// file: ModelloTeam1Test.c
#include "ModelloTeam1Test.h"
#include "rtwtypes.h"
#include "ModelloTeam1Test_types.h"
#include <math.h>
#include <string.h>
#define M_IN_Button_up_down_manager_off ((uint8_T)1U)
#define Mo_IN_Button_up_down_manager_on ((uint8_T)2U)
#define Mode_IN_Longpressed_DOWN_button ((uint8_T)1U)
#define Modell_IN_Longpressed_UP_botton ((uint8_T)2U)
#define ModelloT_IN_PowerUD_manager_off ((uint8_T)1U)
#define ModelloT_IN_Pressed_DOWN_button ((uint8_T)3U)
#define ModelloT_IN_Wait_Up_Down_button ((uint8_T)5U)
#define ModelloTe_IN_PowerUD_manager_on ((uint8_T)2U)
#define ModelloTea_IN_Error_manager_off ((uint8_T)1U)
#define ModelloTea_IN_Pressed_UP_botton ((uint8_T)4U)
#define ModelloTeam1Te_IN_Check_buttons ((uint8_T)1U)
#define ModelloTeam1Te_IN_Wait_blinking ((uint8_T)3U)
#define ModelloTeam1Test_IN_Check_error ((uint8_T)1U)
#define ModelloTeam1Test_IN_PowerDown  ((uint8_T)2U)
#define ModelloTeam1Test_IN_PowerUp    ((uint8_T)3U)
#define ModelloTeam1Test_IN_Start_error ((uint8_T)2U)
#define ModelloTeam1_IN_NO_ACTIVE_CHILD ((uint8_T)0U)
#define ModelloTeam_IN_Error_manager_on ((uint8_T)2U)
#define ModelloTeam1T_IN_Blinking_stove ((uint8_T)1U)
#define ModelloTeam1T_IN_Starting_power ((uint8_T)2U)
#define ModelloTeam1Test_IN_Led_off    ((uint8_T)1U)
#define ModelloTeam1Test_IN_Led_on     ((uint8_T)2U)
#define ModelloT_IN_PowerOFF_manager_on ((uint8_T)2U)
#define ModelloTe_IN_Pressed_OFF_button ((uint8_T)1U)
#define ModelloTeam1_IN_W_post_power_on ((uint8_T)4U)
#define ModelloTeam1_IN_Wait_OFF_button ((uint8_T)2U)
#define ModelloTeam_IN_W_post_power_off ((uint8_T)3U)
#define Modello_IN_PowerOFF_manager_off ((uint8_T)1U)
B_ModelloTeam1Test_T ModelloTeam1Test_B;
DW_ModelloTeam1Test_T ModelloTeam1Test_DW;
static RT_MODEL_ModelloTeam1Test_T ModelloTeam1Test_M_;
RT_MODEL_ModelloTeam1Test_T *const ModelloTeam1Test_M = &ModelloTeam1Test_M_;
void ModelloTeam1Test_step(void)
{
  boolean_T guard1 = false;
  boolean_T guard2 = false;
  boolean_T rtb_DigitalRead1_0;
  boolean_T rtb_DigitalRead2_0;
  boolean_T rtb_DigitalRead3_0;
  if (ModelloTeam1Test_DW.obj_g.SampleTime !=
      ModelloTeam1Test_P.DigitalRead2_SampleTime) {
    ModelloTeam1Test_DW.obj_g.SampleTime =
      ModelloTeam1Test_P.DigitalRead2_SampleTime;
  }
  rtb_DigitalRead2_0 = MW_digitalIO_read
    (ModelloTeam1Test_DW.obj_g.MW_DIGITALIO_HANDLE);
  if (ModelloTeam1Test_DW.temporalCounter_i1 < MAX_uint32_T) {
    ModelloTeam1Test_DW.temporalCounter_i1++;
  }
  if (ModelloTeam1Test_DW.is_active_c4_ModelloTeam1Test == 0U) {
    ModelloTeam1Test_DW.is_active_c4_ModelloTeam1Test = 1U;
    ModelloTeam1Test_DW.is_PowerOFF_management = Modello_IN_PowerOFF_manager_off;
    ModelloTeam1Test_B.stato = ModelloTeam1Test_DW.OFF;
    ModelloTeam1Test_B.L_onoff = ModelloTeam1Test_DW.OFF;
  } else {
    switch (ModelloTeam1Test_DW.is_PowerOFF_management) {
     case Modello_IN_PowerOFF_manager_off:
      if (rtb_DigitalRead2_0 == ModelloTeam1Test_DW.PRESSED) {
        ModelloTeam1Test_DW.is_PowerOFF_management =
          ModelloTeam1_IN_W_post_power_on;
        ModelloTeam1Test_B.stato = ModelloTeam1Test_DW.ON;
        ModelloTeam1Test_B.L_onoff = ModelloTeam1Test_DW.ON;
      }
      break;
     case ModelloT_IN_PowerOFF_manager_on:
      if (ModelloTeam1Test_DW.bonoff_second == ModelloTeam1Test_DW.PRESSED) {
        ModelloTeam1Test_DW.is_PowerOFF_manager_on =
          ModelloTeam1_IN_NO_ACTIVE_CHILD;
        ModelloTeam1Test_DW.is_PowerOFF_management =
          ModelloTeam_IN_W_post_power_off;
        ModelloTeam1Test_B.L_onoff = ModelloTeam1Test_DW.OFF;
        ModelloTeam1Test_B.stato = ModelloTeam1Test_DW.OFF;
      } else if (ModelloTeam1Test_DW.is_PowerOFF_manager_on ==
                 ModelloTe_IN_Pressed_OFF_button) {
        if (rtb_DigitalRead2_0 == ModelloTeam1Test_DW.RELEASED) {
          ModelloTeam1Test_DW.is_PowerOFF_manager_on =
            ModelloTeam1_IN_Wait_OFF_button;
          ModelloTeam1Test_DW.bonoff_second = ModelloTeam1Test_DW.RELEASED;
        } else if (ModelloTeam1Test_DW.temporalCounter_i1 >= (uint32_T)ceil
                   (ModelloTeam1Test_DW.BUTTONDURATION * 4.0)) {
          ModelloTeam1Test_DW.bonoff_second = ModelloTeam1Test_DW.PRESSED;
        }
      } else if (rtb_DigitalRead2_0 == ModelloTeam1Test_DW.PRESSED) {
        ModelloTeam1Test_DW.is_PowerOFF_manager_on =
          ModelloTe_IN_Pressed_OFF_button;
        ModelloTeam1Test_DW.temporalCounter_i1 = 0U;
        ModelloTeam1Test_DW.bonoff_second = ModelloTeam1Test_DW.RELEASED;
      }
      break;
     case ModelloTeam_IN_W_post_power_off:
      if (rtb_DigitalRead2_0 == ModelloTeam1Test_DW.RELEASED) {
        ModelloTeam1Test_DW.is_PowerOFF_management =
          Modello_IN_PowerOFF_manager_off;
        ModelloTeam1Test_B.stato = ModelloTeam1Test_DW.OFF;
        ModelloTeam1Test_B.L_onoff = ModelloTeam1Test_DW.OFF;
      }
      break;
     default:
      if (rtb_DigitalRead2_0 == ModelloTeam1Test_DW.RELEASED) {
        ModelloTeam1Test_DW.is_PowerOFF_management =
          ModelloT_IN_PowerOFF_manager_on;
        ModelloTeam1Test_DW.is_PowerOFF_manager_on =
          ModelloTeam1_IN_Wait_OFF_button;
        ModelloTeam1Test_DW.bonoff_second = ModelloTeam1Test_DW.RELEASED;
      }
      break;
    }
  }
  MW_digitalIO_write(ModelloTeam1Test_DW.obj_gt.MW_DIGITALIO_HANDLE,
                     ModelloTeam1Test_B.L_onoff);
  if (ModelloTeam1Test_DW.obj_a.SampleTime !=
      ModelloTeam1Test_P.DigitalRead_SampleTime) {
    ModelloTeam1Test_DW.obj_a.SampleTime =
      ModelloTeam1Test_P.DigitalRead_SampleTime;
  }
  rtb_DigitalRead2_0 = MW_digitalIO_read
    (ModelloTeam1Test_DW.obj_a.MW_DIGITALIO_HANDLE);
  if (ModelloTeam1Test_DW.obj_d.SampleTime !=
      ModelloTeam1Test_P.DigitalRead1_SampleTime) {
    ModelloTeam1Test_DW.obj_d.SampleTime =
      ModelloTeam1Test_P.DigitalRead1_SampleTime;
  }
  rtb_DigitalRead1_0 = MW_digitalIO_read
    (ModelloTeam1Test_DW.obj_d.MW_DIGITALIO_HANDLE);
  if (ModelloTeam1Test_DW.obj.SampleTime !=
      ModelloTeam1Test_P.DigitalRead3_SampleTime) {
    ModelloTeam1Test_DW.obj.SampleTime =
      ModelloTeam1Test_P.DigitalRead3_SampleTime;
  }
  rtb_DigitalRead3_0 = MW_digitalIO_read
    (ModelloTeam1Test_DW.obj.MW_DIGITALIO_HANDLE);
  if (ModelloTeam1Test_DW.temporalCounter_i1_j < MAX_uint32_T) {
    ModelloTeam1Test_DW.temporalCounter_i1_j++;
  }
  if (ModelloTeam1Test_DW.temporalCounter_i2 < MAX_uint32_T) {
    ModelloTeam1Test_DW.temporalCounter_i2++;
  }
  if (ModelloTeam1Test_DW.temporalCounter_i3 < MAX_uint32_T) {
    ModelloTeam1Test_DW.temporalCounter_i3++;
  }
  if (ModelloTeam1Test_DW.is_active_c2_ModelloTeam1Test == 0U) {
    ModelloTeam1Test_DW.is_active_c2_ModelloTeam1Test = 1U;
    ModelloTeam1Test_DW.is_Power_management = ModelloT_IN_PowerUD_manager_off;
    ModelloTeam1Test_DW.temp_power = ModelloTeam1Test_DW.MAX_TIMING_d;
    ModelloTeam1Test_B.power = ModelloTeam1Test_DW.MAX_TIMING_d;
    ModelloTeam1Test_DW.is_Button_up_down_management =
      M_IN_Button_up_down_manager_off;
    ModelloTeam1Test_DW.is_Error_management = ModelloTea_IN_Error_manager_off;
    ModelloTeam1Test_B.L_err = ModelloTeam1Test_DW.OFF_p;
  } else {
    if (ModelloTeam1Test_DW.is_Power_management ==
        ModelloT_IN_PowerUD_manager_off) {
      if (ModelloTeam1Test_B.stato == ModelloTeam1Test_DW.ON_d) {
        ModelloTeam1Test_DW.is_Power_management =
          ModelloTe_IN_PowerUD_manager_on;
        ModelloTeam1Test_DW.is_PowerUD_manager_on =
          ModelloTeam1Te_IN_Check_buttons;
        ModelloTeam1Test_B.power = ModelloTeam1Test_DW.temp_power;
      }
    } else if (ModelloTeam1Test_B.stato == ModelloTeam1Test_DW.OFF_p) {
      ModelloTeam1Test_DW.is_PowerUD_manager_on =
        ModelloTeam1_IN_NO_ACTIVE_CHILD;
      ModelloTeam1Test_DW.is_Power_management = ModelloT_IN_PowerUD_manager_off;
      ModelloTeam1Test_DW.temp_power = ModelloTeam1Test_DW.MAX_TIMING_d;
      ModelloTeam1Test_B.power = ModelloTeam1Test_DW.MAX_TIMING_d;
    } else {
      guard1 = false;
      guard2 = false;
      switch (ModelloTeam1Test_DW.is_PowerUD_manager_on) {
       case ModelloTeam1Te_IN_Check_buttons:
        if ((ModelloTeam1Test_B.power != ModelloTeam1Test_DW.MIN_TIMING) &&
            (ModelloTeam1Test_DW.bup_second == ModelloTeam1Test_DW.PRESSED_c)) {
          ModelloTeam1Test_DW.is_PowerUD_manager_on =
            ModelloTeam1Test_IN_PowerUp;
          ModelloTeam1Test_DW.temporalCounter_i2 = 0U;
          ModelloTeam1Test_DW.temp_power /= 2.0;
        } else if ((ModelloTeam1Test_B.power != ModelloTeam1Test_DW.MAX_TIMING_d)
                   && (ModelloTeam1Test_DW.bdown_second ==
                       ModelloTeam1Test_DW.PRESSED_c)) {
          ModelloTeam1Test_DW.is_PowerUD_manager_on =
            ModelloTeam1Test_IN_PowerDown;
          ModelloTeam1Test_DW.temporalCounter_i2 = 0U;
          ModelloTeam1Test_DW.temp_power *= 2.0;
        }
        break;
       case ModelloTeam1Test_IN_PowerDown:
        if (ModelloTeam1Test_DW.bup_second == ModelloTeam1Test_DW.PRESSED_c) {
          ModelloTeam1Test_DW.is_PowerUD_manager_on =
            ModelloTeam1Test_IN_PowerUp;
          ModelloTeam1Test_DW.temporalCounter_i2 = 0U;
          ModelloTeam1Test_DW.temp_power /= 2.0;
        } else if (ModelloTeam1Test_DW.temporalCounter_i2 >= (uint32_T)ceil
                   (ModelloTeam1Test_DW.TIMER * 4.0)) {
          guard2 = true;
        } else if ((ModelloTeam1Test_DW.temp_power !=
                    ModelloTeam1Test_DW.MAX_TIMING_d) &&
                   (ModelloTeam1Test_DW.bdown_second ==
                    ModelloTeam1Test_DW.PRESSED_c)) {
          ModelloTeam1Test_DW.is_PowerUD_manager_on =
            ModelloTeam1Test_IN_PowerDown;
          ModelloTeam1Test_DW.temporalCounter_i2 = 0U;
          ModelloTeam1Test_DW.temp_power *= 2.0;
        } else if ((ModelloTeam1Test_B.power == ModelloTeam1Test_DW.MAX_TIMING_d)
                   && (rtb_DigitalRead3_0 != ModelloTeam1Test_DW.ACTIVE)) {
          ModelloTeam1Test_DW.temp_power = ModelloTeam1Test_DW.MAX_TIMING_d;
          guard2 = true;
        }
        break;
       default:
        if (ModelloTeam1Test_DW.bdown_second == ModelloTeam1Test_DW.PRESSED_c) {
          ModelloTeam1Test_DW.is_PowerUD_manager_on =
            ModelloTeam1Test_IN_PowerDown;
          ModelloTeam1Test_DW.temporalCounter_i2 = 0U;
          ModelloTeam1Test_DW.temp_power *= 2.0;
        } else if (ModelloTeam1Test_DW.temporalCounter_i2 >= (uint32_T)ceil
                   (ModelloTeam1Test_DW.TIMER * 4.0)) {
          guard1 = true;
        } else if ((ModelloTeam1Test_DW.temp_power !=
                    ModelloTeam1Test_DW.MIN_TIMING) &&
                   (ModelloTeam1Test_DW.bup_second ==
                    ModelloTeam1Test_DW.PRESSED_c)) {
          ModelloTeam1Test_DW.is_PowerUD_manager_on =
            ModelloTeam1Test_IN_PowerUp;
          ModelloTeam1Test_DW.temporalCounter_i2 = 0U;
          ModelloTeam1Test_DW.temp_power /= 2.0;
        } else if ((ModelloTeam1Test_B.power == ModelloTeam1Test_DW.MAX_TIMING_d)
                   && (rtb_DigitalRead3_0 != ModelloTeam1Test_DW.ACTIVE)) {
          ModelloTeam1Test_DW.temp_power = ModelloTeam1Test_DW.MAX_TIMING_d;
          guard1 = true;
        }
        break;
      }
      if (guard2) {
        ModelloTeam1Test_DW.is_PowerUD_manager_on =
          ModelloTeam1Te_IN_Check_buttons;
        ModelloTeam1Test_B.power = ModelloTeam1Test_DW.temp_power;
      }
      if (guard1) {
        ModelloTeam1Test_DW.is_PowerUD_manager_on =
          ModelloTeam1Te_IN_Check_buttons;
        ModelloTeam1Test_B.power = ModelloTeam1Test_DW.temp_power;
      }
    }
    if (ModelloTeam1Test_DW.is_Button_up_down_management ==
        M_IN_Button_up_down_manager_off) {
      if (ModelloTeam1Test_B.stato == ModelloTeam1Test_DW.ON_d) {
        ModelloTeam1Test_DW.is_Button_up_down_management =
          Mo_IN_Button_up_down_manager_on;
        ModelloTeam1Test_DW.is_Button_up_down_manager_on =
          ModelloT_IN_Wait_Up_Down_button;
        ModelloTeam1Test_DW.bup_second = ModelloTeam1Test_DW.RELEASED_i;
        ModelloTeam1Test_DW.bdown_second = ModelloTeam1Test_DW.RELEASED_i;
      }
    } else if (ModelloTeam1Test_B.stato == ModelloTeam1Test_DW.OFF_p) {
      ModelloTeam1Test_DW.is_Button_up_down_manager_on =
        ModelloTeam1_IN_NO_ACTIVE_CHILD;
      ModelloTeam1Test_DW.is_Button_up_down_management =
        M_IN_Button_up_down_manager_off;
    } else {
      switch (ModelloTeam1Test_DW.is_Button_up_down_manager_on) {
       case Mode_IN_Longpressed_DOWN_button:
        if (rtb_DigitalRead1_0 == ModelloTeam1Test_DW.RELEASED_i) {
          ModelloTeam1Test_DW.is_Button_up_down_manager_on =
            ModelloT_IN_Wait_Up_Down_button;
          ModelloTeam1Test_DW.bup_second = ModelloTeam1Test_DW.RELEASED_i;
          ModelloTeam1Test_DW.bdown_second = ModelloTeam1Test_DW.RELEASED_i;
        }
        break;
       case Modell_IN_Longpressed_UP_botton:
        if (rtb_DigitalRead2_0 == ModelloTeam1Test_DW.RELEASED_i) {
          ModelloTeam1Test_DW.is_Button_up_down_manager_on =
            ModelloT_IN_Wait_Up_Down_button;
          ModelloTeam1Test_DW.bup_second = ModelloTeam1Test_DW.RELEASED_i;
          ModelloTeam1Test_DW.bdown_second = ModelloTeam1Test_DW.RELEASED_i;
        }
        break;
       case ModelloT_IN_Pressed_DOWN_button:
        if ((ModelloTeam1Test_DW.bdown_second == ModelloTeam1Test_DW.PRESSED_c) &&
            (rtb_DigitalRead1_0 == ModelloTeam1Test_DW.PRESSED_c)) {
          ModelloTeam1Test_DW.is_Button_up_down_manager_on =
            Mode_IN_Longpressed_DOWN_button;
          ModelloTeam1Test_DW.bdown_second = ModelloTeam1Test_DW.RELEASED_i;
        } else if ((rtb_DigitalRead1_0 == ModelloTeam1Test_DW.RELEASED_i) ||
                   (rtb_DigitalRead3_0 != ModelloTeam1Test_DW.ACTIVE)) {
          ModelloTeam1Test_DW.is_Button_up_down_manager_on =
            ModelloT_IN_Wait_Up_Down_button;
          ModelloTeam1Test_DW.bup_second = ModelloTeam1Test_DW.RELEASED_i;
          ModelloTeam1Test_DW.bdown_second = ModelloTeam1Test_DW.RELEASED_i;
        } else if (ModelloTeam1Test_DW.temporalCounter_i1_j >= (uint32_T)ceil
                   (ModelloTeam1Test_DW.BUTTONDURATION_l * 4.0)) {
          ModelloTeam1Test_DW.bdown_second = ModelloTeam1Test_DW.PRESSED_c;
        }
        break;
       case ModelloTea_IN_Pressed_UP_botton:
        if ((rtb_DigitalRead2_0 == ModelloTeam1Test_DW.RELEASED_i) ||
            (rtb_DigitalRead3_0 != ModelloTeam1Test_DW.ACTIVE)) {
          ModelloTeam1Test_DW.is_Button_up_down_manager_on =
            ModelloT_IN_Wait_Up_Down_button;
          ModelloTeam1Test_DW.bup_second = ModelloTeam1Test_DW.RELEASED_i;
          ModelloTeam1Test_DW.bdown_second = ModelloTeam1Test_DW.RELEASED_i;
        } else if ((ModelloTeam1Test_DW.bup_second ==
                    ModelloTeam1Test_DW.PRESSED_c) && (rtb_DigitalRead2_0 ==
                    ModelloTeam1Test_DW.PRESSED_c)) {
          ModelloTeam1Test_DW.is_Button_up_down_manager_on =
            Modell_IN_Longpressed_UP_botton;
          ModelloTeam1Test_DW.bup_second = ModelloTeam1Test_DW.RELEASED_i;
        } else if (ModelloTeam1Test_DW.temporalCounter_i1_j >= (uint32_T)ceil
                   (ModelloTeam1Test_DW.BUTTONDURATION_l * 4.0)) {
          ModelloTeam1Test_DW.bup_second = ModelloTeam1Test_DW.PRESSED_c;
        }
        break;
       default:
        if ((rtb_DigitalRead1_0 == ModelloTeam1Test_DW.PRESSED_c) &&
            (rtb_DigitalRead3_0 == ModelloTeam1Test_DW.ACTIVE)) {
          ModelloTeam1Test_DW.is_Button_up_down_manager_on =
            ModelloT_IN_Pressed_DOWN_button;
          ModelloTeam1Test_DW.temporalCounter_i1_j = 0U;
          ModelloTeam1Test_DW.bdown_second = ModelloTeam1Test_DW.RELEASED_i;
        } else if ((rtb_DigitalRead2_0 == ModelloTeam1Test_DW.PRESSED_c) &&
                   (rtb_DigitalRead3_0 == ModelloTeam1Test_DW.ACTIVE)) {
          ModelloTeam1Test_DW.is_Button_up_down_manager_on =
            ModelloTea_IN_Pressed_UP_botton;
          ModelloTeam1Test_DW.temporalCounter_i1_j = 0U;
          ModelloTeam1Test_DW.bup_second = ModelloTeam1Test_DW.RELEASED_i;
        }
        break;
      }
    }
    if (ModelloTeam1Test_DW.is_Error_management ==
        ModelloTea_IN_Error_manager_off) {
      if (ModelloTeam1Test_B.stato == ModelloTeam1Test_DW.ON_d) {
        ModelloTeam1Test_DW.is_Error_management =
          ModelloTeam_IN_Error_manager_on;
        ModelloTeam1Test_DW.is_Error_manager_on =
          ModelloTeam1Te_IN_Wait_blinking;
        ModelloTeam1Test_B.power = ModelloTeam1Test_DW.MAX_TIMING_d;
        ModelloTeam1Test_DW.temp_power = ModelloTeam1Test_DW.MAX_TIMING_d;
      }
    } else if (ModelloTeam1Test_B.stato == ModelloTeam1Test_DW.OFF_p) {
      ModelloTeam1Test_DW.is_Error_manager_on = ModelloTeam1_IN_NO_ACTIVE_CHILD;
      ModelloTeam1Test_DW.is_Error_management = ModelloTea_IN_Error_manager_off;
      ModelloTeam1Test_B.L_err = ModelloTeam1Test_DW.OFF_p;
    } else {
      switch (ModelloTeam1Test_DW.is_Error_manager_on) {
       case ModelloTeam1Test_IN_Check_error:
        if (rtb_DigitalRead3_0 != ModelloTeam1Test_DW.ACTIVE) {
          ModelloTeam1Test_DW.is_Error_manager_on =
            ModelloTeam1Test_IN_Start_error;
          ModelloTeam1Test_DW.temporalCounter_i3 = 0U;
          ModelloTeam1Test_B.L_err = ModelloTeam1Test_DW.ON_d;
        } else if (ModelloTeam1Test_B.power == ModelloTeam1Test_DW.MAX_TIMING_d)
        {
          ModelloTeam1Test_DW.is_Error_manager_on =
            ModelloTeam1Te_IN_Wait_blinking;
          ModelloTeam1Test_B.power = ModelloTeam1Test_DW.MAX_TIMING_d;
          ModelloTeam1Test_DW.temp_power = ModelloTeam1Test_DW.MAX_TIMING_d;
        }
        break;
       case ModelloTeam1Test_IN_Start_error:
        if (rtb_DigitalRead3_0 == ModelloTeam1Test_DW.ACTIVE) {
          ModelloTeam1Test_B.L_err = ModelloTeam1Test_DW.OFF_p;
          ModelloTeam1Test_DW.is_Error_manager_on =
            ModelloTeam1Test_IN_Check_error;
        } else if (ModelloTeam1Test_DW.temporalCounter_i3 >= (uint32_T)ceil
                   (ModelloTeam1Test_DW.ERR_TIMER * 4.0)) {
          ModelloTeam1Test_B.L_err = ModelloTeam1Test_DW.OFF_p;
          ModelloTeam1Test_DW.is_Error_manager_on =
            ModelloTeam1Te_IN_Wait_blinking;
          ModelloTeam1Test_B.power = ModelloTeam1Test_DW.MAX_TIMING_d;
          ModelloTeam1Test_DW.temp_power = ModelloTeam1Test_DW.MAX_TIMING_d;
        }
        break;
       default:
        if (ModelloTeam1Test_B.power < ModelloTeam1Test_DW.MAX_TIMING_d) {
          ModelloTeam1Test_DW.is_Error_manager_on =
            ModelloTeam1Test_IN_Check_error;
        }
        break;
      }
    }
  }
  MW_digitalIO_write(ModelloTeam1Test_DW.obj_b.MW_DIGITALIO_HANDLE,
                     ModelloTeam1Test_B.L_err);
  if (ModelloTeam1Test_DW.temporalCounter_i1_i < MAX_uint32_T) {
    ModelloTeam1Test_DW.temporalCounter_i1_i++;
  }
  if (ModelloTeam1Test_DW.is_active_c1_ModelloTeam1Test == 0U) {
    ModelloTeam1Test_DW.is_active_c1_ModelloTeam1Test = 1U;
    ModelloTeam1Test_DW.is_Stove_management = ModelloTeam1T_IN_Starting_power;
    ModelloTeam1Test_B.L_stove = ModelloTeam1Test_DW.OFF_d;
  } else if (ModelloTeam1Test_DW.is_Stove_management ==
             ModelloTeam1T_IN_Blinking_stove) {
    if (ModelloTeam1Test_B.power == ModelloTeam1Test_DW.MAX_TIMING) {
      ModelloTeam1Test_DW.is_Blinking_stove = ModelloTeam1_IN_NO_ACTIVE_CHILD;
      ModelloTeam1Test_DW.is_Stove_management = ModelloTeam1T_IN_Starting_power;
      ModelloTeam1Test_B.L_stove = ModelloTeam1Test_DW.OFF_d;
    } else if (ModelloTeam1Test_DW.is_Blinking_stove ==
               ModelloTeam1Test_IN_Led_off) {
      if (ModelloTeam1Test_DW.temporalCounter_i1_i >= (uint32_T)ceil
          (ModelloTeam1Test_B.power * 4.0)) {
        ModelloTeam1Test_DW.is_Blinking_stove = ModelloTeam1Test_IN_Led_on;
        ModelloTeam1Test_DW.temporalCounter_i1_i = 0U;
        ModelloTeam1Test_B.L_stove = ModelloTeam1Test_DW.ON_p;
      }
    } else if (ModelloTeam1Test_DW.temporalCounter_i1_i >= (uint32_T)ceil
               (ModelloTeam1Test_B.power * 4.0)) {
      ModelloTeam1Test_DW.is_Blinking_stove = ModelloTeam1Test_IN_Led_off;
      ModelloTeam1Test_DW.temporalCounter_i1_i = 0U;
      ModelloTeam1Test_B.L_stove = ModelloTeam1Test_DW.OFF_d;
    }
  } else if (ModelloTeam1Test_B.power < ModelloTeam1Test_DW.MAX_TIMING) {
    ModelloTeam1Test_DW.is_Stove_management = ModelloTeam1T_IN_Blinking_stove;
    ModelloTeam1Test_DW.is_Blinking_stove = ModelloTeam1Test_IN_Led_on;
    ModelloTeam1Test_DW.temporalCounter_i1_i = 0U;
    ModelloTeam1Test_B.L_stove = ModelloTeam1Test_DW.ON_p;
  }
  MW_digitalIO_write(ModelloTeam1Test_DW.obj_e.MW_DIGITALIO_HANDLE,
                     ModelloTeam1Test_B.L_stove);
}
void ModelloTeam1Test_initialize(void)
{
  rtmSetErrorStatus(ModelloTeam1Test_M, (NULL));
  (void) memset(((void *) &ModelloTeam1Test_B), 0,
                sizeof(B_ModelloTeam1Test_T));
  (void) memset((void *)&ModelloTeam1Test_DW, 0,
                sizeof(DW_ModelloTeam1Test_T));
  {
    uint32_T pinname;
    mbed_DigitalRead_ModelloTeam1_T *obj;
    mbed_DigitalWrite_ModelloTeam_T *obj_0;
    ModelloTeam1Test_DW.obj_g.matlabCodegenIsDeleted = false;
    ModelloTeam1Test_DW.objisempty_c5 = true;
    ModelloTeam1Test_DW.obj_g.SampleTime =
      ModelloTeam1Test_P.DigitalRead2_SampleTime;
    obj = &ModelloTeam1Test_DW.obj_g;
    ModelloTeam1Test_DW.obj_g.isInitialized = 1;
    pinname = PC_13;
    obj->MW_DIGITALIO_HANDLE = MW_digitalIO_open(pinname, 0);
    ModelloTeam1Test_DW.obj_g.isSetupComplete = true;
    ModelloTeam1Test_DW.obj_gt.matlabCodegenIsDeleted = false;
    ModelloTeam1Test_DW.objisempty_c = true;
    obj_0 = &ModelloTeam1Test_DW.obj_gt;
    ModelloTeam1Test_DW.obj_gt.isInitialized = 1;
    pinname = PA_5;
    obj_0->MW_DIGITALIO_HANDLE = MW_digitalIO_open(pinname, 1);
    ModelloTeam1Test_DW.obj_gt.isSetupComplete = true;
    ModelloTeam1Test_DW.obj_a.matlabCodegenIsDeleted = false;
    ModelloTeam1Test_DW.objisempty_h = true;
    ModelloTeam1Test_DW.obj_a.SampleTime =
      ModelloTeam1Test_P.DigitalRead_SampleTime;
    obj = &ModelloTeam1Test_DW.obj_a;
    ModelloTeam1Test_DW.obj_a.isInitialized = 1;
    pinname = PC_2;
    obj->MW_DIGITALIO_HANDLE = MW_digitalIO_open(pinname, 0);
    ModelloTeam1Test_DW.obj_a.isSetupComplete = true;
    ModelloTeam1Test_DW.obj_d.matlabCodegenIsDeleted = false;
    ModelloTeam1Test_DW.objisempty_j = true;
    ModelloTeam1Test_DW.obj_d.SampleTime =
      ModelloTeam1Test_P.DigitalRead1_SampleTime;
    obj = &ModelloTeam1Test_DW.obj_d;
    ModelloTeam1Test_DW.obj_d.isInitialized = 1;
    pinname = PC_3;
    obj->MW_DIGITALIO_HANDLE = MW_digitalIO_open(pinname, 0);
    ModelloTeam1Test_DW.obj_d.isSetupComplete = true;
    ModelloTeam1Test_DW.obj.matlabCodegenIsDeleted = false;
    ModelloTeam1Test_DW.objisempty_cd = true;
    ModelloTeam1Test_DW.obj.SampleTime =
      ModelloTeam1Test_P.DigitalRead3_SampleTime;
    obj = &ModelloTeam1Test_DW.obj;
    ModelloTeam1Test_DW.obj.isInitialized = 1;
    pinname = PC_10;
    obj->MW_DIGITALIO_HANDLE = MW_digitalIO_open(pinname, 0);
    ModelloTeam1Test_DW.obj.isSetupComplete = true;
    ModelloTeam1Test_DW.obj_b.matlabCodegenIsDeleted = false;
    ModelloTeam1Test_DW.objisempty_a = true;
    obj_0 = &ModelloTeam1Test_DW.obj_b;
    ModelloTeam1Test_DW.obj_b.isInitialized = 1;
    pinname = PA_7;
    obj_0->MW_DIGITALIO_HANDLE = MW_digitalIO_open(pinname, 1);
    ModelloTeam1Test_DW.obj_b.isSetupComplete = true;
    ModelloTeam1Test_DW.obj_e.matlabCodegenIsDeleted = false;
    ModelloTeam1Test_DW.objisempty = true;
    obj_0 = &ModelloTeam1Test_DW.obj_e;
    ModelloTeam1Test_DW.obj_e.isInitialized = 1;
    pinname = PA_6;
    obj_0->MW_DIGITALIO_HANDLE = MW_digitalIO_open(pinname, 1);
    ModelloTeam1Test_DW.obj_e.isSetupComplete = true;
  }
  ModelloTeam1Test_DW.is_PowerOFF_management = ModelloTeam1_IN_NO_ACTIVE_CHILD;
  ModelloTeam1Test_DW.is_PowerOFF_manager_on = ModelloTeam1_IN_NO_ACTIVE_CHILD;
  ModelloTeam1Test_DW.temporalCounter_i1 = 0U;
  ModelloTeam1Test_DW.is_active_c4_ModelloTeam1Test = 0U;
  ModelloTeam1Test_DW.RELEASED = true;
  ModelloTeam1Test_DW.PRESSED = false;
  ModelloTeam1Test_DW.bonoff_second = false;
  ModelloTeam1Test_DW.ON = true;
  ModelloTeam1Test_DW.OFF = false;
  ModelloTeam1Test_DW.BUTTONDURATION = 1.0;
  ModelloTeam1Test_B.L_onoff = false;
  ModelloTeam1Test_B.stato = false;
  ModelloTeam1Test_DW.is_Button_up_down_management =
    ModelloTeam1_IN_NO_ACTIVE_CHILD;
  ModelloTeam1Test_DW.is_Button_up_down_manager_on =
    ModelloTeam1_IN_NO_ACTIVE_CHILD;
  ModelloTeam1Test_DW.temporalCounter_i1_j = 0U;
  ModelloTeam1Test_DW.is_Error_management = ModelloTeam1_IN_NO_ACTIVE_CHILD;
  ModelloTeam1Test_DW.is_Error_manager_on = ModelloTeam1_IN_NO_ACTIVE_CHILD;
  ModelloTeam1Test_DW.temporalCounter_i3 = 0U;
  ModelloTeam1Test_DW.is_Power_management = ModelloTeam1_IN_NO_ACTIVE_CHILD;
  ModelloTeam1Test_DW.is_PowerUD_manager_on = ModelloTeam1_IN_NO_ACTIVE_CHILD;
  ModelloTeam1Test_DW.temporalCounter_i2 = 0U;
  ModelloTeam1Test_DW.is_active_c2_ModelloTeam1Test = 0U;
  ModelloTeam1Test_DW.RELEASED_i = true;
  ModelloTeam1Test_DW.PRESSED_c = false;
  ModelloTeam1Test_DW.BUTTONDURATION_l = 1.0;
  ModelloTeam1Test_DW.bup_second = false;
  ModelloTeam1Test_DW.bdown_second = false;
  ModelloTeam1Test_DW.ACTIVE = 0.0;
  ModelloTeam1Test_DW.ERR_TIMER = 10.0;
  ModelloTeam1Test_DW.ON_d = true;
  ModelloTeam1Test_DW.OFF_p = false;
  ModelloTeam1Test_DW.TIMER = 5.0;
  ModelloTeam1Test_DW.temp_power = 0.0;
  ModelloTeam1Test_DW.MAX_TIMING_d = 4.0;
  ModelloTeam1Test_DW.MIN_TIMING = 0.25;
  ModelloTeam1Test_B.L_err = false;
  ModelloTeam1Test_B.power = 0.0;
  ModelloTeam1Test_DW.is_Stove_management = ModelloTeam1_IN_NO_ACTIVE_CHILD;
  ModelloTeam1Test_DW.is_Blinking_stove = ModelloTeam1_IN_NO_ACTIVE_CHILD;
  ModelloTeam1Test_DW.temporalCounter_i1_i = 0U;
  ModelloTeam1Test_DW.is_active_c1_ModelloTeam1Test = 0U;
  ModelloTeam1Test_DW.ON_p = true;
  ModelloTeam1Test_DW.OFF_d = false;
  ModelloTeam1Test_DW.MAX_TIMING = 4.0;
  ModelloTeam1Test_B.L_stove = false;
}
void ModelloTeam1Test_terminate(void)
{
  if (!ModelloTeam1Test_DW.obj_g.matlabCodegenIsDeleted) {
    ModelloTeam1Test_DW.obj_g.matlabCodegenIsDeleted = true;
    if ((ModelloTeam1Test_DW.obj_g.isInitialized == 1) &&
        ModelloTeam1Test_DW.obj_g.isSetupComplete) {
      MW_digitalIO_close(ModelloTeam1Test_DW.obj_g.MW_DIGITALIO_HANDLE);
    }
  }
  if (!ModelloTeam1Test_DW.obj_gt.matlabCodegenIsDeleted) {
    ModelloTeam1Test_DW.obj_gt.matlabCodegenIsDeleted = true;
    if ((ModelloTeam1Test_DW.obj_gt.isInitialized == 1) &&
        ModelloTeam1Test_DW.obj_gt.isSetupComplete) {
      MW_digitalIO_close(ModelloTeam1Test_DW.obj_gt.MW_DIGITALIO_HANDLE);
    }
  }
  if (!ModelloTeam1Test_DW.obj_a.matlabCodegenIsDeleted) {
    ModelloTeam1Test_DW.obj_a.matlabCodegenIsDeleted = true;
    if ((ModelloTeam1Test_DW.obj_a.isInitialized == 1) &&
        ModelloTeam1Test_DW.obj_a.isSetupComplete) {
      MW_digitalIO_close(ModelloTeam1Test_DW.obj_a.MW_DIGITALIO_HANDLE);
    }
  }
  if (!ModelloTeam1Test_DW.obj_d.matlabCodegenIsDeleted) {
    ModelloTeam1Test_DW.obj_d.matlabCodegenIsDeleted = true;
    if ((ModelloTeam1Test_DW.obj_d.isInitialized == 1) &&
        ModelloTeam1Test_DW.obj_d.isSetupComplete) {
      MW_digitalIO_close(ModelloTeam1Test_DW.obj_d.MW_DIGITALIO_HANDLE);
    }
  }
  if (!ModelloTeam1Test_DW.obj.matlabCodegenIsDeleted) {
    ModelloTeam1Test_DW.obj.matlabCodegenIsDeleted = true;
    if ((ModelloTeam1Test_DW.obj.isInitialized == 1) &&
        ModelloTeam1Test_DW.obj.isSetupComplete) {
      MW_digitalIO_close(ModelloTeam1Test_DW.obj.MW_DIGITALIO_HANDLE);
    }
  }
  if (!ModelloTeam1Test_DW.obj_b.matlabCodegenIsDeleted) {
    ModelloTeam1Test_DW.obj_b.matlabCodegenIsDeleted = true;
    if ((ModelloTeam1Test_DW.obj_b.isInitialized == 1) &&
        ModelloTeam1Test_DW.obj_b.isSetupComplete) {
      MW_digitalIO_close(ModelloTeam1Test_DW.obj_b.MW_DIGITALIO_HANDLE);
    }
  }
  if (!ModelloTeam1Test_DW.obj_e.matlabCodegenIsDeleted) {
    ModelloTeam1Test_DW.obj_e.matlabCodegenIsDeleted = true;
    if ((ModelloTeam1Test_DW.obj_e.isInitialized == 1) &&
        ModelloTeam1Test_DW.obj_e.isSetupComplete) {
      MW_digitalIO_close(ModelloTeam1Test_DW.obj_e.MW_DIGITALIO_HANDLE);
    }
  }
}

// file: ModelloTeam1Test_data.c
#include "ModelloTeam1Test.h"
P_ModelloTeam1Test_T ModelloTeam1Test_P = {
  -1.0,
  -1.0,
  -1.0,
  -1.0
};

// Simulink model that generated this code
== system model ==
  DigitalWrite : mbedblockslib/Digital Write  <- 1: Stateflowchart#1
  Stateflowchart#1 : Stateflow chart  <- 1: DigitalRead2
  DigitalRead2 : mbedblockslib/Digital Read
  DigitalWrite#1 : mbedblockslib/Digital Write  <- 1: Stateflowchart#2
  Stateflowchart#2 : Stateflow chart  <- 1: DigitalRead, 2: DigitalRead1, 3: DigitalRead3, 4: Stateflowchart#1/2
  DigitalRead : mbedblockslib/Digital Read
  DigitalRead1 : mbedblockslib/Digital Read
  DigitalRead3 : mbedblockslib/Digital Read
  DigitalWrite#2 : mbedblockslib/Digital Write  <- 1: Stateflowchart#3
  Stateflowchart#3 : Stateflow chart  <- 1: Stateflowchart#2/2
== stateflow chart Stateflowchart#3 ==
  state Stove_management
    state Blinking_stove
      state Led_on
        en: L_stove=ON;
      state Led_off
        en: L_stove = OFF;
      (default) -> Led_on
      Led_off -> Led_on : after(power,sec)
      Led_on -> Led_off : after(power,sec)
    state Starting_power
      en: L_stove=OFF;
    (default) -> Starting_power
    Blinking_stove -> Starting_power : [power==MAX_TIMING]
    Starting_power -> Blinking_stove : [power<MAX_TIMING]
  data: ON local =true; OFF local =false; L_stove output; power input; MAX_TIMING local =4

== stateflow chart Stateflowchart#2 ==
  state Power_and_error_management
    state Power_management [parallel]
      settings: executionOrder=1
      state PowerUD_manager_on
        state PowerUp
          en: temp_power=temp_power/2
        state Check_buttons
          en: power=temp_power;
        state PowerDown
          en: temp_power=temp_power*2
        PowerUp -> Check_buttons [order 4] : [power==MAX_TIMING & sensor~=ACTIVE]{temp_power=MAX_TIMING}
        PowerUp -> Check_buttons [order 2] : after(TIMER,sec)
        Check_buttons -> PowerUp [order 1] : [power~=MIN_TIMING  & bup_second==PRESSED]
        PowerUp -> PowerUp [order 3] : [temp_power~=MIN_TIMING  & bup_second==PRESSED]
        PowerUp -> PowerDown [order 1] : [bdown_second==PRESSED]
        PowerDown -> PowerUp [order 1] : [ bup_second==PRESSED]
        (default) -> Check_buttons
        Check_buttons -> PowerDown [order 2] : [power~=MAX_TIMING & bdown_second==PRESSED]
        PowerDown -> Check_buttons [order 4] : [power==MAX_TIMING & sensor~=ACTIVE]{temp_power=MAX_TIMING}
        PowerDown -> Check_buttons [order 2] : after(TIMER,sec)
        PowerDown -> PowerDown [order 3] : [temp_power~=MAX_TIMING & bdown_second==PRESSED]
      state PowerUD_manager_off
        en: temp_power=MAX_TIMING
        power=MAX_TIMING;
      (default) -> PowerUD_manager_off
      PowerUD_manager_off -> PowerUD_manager_on : [stato==ON]
      PowerUD_manager_on -> PowerUD_manager_off : [stato==OFF]
    state Button_up_down_management [parallel]
      settings: executionOrder=2
      state Button_up_down_manager_on
        state Longpressed_DOWN_button
          en: bdown_second = RELEASED;
        state Longpressed_UP_botton
          en: bup_second = RELEASED;
        state Pressed_DOWN_button
          en: bdown_second = RELEASED;
          on after(BUTTONDURATION,sec):
          bdown_second=PRESSED;
        state Pressed_UP_botton
          en: bup_second = RELEASED;
          on after(BUTTONDURATION,sec):
          bup_second=PRESSED;
        state Wait_Up_Down_button
          en: bup_second=RELEASED;
          bdown_second=RELEASED;
        Longpressed_UP_botton -> Wait_Up_Down_button : [bup==RELEASED]
        Pressed_UP_botton -> Longpressed_UP_botton [order 2] : [bup_second==PRESSED & bup == PRESSED]
        Pressed_DOWN_button -> Longpressed_DOWN_button [order 1] : [bdown_second==PRESSED & bdown == PRESSED]
        Longpressed_DOWN_button -> Wait_Up_Down_button : [bdown==RELEASED]
        Pressed_UP_botton -> Wait_Up_Down_button [order 1] : [bup==RELEASED | sensor ~=ACTIVE]
        Pressed_DOWN_button -> Wait_Up_Down_button [order 2] : [bdown==RELEASED | sensor~=ACTIVE]
        Wait_Up_Down_button -> Pressed_UP_botton [order 2] : [bup==PRESSED & sensor==ACTIVE]
        (default) -> Wait_Up_Down_button
        Wait_Up_Down_button -> Pressed_DOWN_button [order 1] : [bdown==PRESSED & sensor==ACTIVE]
      state Button_up_down_manager_off
      Button_up_down_manager_off -> Button_up_down_manager_on : [stato==ON]
      Button_up_down_manager_on -> Button_up_down_manager_off : [stato==OFF]
      (default) -> Button_up_down_manager_off
    state Error_management [parallel]
      settings: executionOrder=3
      state Error_manager_on
        state Wait_blinking
          en: power=MAX_TIMING;
          temp_power=MAX_TIMING;
        state Check_error
        state Start_error
          en: L_err=ON;
          ex: L_err =OFF;
        (default) -> Wait_blinking
        Check_error -> Wait_blinking [order 2] : [power==MAX_TIMING]
        Wait_blinking -> Check_error : [power<MAX_TIMING]
        Start_error -> Check_error [order 1] : [sensor==ACTIVE]
        Check_error -> Start_error [order 1] : [sensor~=ACTIVE]
        Start_error -> Wait_blinking [order 2] : after(ERR_TIMER,sec)
      state Error_manager_off
        en: L_err=OFF;
      Error_manager_off -> Error_manager_on : [stato==ON]
      (default) -> Error_manager_off
      Error_manager_on -> Error_manager_off : [stato==OFF]
  (default) -> Power_and_error_management
  data: bup input; bdown input; sensor input; L_err output; RELEASED local =true; PRESSED local =false; BUTTONDURATION local =1; bup_second local; bdown_second local; ACTIVE local =0; ERR_TIMER local =10; ON local =true; OFF local =false; TIMER local =5; temp_power local; power output; stato input boolean; MAX_TIMING local =4; MIN_TIMING local =0.25

== stateflow chart Stateflowchart#1 ==
  state PowerOFF_management
    state PowerOFF_manager_on
      state Pressed_OFF_button
        en: bonoff_second = RELEASED;
        on after(BUTTONDURATION,sec):
        bonoff_second=PRESSED;
      state Wait_OFF_button
        en: bonoff_second=RELEASED;
      Wait_OFF_button -> Pressed_OFF_button : [bonoff == PRESSED]
      Pressed_OFF_button -> Wait_OFF_button : [bonoff==RELEASED]
      (default) -> Wait_OFF_button
    state W_post_power_off
      en: L_onoff=OFF;
      stato=OFF;
    state PowerOFF_manager_off
      en: stato=OFF;
      L_onoff=OFF;
    state W_post_power_on
      en: stato=ON;
      L_onoff=ON;
    PowerOFF_manager_on -> W_post_power_off : [bonoff_second==PRESSED]
    W_post_power_off -> PowerOFF_manager_off : [bonoff==RELEASED]
    W_post_power_on -> PowerOFF_manager_on : [bonoff==RELEASED]
    (default) -> PowerOFF_manager_off
    PowerOFF_manager_off -> W_post_power_on : [bonoff==PRESSED]
  data: L_onoff output; bonoff input; RELEASED local =true; PRESSED local =false; bonoff_second local; ON local =true; OFF local =false; BUTTONDURATION local =1; stato output
